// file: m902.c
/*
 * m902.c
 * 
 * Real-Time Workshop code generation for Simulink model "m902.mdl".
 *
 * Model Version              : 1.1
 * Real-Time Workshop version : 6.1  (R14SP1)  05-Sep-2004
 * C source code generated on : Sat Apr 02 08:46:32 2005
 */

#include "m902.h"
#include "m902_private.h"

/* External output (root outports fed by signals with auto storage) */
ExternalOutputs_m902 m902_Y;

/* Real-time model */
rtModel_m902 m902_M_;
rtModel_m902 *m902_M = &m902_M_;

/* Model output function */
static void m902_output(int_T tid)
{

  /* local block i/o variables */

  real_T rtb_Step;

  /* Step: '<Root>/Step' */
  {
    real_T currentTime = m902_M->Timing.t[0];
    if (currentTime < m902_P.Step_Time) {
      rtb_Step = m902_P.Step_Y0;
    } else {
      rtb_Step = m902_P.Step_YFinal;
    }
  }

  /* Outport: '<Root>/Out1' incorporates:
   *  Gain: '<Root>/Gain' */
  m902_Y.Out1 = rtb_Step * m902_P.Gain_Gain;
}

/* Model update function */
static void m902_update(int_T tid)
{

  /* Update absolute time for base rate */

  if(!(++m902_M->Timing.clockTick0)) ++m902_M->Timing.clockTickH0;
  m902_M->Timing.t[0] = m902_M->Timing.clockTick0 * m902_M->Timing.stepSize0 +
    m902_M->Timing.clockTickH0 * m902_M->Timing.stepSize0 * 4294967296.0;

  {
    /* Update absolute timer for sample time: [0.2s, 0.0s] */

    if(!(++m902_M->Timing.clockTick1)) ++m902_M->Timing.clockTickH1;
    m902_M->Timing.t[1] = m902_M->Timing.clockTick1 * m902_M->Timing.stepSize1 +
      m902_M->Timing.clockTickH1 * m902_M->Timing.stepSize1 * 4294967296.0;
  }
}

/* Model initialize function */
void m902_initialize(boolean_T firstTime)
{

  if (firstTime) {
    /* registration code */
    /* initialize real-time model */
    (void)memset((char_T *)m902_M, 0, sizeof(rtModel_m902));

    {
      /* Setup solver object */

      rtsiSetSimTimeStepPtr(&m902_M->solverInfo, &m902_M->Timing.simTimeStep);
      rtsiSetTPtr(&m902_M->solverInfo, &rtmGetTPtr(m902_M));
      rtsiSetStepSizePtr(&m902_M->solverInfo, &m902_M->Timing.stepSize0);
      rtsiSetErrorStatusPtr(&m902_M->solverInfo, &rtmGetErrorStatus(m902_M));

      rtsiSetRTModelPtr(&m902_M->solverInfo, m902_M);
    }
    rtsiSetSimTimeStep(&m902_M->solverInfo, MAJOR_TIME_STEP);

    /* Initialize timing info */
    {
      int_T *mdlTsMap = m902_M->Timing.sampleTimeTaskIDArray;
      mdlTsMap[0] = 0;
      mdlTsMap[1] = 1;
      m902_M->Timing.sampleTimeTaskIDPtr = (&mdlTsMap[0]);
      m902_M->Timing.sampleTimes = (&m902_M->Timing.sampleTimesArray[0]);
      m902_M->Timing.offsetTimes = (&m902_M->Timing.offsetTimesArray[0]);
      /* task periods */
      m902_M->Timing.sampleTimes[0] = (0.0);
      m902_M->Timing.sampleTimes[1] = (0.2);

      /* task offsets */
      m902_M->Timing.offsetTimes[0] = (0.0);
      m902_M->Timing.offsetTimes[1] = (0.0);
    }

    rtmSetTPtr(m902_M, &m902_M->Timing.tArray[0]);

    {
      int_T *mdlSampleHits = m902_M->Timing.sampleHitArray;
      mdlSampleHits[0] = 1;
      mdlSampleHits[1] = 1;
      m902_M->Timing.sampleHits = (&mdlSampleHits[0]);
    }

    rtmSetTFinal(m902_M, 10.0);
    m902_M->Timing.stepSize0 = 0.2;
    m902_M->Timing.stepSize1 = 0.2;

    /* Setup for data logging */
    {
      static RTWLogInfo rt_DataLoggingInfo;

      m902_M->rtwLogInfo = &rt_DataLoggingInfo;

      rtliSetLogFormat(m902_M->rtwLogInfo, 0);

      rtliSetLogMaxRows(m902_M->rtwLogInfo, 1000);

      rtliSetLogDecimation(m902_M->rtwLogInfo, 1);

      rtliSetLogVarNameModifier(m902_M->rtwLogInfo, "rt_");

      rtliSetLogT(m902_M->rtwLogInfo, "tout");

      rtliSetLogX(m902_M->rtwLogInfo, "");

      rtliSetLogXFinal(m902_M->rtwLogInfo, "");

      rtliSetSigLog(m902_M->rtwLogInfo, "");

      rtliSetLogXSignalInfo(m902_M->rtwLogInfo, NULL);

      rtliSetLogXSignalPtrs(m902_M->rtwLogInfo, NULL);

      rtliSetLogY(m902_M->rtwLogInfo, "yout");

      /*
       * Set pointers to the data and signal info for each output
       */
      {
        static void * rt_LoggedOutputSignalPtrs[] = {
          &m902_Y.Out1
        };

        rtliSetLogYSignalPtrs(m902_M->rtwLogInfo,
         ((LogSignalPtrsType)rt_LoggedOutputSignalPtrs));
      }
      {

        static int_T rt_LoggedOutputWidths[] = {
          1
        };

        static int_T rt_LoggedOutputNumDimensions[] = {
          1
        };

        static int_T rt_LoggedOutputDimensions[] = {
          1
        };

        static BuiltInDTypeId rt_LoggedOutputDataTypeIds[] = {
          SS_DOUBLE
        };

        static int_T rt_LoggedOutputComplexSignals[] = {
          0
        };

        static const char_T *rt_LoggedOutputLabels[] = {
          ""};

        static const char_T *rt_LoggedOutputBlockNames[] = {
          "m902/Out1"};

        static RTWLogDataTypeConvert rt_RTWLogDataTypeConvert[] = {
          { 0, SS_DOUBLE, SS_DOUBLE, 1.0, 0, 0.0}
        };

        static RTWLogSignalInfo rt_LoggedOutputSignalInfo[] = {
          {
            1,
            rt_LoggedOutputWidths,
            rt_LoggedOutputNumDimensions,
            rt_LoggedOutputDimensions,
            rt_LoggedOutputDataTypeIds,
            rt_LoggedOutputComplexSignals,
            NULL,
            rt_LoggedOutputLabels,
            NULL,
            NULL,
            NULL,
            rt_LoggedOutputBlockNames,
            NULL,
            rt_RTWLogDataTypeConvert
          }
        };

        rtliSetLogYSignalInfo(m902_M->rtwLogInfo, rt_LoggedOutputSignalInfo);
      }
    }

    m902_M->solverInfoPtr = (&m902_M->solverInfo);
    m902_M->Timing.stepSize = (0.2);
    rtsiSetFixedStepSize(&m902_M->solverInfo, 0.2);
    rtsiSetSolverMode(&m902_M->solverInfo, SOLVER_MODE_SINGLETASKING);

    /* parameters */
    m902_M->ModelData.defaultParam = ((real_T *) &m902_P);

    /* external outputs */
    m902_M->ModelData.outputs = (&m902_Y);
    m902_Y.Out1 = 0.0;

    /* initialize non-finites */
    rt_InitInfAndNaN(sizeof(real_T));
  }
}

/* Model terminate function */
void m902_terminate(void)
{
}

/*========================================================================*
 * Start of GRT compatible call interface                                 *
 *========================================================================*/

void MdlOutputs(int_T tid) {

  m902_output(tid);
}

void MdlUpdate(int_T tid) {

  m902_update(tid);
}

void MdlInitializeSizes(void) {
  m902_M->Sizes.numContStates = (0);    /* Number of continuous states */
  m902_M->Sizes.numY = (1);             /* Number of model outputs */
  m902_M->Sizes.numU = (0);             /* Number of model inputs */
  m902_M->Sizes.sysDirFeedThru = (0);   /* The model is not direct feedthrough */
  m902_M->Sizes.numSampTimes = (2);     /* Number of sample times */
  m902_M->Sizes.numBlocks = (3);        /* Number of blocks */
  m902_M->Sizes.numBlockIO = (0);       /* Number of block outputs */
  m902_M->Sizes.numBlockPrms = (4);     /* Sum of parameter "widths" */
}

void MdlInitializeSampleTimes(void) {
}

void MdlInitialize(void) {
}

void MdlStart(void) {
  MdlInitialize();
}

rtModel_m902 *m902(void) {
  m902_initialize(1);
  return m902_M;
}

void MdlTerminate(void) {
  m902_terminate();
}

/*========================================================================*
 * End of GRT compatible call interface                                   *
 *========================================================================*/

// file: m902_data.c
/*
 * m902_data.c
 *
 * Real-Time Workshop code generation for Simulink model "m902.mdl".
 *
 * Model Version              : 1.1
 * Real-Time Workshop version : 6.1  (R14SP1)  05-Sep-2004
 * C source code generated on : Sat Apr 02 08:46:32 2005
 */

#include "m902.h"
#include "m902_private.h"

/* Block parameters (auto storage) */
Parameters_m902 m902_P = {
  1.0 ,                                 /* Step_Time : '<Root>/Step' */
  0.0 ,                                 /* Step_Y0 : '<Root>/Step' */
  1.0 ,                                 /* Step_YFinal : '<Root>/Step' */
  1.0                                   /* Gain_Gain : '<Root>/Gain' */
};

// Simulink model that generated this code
simulink model "m902"  (Simulink 6.1)
settings: Solver=FixedStepDiscrete  StartTime=0.0  StopTime=10.0  FixedStep=0.2  RelTol=1e-3

== system m902 ==
  Gain : Gain
  Step : Step  SampleTime=0
  Out1 : Outport
  wires:
  Step/1 -> Gain/1
  Gain/1 -> Out1/1
